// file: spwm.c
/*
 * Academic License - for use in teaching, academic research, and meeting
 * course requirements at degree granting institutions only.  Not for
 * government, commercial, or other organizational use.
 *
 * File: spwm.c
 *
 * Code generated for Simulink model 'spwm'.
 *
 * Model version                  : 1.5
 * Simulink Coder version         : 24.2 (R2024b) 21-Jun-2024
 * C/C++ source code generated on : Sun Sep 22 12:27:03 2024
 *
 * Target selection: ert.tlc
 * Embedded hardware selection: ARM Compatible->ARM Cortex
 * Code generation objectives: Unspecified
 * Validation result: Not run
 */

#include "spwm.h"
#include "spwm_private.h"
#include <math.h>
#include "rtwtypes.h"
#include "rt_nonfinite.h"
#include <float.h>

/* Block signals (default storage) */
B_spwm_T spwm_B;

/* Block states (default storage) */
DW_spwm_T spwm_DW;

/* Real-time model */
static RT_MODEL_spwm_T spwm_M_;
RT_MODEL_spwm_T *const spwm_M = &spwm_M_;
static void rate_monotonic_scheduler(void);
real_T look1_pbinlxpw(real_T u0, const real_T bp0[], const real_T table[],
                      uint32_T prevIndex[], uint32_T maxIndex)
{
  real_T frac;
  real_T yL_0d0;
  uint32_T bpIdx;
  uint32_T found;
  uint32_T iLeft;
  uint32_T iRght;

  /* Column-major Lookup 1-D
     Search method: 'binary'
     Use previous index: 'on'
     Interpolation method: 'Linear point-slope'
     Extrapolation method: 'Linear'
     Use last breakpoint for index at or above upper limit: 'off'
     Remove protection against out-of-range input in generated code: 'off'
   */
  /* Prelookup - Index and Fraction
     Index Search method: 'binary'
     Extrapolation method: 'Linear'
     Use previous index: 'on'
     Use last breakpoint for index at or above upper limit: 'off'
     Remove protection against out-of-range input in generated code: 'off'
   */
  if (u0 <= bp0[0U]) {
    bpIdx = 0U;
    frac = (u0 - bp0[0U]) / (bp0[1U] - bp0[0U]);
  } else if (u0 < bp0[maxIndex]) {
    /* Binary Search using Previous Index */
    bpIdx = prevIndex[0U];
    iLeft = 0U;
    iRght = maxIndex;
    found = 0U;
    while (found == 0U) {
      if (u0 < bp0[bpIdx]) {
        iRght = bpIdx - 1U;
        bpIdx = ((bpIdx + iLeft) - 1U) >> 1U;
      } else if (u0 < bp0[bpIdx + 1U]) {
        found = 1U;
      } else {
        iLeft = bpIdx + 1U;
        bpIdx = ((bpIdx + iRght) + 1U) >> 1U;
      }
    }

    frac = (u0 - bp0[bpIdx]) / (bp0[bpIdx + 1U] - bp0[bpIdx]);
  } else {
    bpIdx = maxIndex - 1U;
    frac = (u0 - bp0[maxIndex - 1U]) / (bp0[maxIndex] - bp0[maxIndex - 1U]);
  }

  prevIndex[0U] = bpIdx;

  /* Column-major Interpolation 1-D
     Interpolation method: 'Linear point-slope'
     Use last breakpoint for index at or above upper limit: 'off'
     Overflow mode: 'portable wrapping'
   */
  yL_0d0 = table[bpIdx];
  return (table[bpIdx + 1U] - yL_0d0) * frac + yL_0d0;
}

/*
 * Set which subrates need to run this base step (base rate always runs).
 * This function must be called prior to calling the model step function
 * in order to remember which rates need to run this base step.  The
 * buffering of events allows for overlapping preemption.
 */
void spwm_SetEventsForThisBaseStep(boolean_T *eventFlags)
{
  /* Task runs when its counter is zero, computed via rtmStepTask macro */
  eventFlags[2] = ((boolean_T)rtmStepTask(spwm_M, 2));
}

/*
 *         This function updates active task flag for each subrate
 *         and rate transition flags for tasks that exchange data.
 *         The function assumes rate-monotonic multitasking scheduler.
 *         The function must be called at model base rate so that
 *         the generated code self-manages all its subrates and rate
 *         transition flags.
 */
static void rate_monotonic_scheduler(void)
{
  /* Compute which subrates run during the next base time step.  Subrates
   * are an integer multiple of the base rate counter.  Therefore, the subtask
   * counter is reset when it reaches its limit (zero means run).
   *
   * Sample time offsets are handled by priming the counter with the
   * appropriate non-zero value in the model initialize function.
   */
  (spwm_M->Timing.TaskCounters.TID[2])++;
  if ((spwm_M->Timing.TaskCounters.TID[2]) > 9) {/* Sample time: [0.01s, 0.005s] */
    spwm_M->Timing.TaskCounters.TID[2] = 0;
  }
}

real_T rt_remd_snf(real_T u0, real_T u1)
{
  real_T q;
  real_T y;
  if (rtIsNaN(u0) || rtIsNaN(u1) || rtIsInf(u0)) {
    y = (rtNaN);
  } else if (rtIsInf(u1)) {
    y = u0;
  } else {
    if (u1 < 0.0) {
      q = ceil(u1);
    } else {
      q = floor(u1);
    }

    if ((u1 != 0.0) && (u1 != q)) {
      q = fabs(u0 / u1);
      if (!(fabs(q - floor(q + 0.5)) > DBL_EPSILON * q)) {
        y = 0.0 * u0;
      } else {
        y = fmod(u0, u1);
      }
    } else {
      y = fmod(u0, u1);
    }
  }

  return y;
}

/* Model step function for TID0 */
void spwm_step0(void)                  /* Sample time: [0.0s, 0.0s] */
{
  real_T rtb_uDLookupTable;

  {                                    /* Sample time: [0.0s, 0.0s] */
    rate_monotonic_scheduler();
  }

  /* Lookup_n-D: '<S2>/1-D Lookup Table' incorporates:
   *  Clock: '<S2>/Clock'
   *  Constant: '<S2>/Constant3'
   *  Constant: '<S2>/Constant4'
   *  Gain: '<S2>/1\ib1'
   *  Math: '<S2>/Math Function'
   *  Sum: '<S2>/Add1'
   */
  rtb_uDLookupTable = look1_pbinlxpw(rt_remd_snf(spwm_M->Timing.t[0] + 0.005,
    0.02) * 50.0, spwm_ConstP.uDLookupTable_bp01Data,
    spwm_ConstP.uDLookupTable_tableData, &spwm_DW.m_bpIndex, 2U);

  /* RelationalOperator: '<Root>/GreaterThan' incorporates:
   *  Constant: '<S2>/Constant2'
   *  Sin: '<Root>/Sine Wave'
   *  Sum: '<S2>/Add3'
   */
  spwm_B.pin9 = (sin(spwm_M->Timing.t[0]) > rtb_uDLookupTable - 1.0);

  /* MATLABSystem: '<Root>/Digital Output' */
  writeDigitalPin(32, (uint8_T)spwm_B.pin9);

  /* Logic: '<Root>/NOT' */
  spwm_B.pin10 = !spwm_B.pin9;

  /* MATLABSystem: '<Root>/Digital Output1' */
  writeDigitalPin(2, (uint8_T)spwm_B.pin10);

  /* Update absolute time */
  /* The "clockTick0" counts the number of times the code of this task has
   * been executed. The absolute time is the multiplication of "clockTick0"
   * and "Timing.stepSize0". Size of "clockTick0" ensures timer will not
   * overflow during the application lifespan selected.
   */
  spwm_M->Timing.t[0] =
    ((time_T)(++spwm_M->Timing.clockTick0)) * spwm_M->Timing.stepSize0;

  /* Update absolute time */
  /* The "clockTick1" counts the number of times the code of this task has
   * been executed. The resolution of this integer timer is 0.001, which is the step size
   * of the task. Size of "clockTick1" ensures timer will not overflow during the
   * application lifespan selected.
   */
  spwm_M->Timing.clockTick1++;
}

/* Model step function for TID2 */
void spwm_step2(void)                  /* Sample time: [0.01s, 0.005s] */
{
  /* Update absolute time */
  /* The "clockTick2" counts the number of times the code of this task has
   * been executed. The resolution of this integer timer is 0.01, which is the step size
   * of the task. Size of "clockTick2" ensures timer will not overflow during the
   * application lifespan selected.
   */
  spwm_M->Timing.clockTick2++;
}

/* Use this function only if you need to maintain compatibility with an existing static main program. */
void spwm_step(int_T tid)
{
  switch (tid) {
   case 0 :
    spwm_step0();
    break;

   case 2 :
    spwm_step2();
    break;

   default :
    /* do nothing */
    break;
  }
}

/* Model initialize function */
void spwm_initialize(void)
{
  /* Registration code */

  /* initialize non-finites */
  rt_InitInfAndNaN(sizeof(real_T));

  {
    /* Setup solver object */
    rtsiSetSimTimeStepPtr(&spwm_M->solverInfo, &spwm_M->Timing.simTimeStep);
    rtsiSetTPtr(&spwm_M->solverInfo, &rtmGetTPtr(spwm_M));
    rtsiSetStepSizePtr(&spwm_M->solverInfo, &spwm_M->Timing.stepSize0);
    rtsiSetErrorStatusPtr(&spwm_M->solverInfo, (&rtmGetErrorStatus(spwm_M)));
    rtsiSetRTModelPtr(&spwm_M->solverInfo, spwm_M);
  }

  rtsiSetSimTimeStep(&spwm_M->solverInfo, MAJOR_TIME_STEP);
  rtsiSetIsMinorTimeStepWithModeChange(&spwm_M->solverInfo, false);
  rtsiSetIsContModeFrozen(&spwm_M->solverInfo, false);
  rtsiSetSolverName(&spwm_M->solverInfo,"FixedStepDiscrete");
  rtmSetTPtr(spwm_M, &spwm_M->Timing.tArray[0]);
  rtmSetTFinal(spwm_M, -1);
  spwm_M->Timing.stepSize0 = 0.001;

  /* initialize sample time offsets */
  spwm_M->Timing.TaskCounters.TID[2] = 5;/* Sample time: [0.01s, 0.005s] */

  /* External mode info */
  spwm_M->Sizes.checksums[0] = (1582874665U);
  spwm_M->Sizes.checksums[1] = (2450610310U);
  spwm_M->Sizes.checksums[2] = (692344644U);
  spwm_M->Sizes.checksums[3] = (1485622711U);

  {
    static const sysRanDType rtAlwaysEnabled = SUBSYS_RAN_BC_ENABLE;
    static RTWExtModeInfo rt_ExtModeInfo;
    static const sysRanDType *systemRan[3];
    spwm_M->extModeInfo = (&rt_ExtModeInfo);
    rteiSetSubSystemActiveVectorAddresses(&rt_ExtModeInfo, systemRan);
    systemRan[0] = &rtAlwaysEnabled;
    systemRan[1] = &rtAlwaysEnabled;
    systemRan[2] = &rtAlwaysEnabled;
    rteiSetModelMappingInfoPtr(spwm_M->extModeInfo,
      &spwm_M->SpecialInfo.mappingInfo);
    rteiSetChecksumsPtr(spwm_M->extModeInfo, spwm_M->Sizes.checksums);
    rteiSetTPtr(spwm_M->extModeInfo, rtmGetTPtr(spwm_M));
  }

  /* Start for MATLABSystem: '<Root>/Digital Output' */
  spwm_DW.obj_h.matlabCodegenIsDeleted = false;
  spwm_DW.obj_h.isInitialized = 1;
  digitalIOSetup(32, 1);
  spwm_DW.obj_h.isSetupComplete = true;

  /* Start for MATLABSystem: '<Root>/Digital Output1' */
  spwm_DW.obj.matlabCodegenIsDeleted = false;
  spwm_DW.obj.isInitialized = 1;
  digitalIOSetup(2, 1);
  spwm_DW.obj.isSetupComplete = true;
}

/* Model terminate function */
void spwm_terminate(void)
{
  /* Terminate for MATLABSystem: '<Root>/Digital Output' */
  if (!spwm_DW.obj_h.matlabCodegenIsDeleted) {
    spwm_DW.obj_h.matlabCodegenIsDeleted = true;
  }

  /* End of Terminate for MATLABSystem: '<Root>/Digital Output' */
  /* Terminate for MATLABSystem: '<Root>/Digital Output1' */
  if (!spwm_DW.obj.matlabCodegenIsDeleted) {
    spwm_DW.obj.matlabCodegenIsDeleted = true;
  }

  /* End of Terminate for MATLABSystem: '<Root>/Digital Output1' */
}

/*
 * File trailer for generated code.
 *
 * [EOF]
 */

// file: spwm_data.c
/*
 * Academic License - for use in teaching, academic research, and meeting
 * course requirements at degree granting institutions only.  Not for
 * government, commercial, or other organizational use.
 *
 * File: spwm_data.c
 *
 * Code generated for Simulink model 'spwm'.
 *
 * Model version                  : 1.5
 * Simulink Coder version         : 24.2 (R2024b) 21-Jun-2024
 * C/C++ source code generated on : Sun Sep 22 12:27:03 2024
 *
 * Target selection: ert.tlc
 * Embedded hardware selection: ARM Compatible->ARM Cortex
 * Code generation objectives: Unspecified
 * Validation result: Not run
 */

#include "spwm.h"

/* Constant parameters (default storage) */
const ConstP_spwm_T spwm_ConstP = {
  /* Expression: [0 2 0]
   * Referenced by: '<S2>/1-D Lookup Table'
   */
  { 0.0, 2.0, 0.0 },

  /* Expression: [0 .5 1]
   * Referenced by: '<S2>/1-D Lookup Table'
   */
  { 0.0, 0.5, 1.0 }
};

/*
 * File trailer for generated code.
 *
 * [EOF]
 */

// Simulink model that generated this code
simulink model "spwm"  (R2024b)
settings: Solver=FixedStepAuto  StartTime=0.0  StopTime=inf  FixedStep=0.001  RelTol=1e-3  EnableMultiTasking=on
libraries: arduinolib x2, spsTriangleGeneratorLib x1

== system spwm ==
  Digital Output : arduinolib/Digital Output  pinNumber=32  Direction=output  blockPlatform=arduino
  Digital Output1 : arduinolib/Digital Output  pinNumber=2  Direction=output  blockPlatform=arduino
  GreaterThan : RelationalOperator  Operator=>  OutDataTypeStr=boolean  RndMeth=Simplest  InputSameDT=off
  NOT : Logic  Operator=NOT  IconShape=distinctive  AllPortsSameDT=off  OutDataTypeStr=boolean
  Pulse Generator : DiscretePulseGenerator  Commented=on  Period=1000  PulseWidth=500  SampleTime=0.001
  Sine Wave : Sin  Samples=1000  SampleTime=0
  Triangle Generator : spsTriangleGeneratorLib/Triangle Generator  Freq=50  Phase=90  Ts=0
  wires:
  Sine Wave/1 -> GreaterThan/1
  Triangle Generator/1 -> GreaterThan/2
  GreaterThan/1 -> NOT/1, Digital Output/1  "pin 9"
  NOT/1 -> Digital Output1/1  "pin 10"
